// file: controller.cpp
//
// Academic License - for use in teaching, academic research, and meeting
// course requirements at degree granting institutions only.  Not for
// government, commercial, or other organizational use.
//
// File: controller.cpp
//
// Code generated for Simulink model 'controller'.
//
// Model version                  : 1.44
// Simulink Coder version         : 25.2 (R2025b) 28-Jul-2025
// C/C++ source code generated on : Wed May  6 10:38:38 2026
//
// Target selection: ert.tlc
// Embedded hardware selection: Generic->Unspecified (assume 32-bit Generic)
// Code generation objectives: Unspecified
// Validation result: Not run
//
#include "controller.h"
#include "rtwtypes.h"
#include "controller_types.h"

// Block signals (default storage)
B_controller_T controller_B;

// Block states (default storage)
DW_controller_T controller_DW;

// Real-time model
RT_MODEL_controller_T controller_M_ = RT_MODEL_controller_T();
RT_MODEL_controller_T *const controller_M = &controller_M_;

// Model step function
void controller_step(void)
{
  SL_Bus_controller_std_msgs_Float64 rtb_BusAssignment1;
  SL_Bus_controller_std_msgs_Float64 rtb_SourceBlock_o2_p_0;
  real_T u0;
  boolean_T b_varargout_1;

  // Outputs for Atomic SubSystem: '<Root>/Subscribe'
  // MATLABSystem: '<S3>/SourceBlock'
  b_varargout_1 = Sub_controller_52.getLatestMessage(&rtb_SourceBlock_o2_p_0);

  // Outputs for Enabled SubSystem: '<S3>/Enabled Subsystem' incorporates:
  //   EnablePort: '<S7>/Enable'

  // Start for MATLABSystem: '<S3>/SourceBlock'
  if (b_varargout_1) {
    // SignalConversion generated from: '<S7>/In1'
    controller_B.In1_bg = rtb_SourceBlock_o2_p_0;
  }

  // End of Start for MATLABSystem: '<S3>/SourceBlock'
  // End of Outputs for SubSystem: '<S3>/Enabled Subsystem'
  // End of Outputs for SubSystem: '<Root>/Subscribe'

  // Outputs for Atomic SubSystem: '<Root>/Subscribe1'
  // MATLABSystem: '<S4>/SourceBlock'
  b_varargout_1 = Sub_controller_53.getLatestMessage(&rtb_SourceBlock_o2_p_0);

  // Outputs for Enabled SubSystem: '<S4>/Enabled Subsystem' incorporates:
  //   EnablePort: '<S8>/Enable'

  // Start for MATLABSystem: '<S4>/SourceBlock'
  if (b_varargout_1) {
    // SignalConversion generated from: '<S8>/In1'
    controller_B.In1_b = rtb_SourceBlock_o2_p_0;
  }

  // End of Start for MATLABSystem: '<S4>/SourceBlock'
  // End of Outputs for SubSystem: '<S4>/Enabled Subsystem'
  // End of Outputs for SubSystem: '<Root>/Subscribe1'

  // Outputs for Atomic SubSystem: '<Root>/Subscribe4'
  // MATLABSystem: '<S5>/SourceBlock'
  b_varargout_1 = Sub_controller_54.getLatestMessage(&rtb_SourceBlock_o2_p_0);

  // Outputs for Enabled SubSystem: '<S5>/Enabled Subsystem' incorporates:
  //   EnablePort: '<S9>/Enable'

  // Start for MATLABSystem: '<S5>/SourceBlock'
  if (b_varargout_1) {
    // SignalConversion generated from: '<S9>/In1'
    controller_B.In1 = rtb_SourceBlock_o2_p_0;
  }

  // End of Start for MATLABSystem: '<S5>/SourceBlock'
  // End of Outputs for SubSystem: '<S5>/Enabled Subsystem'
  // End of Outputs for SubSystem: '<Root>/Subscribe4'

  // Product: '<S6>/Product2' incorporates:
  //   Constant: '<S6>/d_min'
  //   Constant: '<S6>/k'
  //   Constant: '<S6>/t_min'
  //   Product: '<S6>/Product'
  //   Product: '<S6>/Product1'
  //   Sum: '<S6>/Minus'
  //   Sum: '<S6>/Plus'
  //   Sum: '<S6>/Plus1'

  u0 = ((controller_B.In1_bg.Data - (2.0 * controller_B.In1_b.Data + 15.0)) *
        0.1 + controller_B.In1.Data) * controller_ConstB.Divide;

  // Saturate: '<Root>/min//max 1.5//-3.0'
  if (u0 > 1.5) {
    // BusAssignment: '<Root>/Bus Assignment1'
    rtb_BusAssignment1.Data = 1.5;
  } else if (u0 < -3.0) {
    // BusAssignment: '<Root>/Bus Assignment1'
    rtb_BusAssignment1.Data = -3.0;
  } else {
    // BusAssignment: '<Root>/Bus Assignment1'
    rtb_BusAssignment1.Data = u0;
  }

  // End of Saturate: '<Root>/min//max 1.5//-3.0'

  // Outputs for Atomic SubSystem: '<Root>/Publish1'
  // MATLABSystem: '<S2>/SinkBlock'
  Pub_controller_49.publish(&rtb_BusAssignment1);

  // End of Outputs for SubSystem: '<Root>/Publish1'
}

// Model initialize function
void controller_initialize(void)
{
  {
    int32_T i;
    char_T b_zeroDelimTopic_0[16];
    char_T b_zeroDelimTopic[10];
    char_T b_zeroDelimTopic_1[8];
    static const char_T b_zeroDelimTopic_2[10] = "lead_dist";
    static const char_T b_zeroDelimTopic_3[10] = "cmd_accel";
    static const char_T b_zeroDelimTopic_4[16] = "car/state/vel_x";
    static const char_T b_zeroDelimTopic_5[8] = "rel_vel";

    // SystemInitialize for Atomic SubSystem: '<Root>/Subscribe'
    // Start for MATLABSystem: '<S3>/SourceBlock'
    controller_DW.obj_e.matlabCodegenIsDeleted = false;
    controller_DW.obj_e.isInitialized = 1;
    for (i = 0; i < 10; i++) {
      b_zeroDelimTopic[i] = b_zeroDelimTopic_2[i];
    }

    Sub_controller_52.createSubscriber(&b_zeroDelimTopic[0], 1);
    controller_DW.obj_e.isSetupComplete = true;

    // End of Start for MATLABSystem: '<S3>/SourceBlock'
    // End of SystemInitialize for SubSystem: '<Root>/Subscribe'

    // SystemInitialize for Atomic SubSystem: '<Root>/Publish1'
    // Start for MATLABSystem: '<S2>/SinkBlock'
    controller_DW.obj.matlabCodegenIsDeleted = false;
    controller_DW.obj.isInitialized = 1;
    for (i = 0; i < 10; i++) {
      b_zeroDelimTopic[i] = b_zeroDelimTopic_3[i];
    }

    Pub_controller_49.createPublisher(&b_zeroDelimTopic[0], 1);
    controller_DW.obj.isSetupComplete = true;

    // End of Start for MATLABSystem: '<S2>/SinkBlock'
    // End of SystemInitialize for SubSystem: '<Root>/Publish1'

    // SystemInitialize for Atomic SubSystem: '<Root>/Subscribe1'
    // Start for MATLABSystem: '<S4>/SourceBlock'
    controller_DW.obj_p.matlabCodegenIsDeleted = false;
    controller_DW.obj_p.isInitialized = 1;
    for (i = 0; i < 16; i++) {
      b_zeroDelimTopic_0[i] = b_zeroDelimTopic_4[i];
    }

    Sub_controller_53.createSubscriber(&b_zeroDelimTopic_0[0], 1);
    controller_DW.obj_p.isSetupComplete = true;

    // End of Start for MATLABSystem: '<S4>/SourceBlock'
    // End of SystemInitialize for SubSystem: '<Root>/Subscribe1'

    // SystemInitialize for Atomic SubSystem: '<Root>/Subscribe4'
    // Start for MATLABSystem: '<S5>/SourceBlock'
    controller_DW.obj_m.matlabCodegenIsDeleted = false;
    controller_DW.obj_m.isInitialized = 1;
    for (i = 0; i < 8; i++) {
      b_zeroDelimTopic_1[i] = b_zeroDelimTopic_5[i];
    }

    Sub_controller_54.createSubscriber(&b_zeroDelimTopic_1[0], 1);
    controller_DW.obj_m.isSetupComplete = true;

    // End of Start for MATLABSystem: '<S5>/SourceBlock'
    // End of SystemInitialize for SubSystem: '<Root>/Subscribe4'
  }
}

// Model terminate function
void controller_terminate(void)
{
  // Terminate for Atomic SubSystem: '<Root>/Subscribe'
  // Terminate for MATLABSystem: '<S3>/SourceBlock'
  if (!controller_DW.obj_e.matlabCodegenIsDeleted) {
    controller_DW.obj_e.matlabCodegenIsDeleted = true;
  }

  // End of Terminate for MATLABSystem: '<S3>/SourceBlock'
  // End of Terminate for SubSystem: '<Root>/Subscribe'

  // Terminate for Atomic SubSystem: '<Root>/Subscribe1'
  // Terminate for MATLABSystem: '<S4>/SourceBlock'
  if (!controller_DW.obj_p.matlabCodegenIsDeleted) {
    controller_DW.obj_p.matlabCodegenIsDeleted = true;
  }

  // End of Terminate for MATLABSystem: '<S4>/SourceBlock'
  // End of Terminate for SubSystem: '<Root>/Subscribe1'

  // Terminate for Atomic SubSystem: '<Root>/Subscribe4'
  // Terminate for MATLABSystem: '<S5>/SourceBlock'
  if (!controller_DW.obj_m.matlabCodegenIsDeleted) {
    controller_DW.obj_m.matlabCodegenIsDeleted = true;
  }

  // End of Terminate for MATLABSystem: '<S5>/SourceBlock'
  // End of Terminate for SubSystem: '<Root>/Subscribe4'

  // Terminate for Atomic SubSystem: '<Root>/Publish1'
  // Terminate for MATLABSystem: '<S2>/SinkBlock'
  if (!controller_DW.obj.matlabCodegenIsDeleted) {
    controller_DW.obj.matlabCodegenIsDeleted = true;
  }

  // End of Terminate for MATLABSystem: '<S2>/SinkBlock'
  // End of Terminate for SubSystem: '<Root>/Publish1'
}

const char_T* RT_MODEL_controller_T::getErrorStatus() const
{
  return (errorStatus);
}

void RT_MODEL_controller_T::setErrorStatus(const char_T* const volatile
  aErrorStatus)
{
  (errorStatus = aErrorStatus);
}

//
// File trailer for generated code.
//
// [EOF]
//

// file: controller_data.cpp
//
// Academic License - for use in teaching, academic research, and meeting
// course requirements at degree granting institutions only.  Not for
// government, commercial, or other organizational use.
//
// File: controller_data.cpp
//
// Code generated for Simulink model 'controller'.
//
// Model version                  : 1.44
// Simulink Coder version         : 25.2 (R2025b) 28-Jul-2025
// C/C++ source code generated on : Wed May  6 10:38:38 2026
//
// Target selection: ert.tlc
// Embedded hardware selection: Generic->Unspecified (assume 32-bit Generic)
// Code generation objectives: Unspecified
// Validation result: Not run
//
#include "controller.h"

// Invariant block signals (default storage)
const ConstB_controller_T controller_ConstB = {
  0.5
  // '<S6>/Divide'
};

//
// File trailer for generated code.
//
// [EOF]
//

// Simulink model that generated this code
simulink model "controller"  (R2025b)
settings: Solver=FixedStepAuto  StartTime=0.0  StopTime=inf  FixedStep=0.05  RelTol=1e-3
libraries: robotlib x5

== system controller ==
  note: This block subscribes
      | to relative distance
  Blank Message1 : robotlib/Blank Message  messageClass=Message  entityType=std_msgs/Float64  messageType=std_msgs/Float64  SampleTime=inf  legacyBusStruct=off
  Bus Assignment1 : BusAssignment  AssignedSignals=Data
  Bus Selector1 : BusSelector  OutputSignals=Data
  Bus Selector4 : BusSelector  OutputSignals=Data
  Bus Selector6 : BusSelector  OutputSignals=Data
  Publish1 : robotlib/Publish  topicSource=Specify your own  topic=cmd_accel  messageType=std_msgs/Float64  legacyBusStruct=off  messageQueueLength=1
  Subscribe : robotlib/Subscribe  topicSource=Specify your own  topic=lead_dist  messageType=std_msgs/Float64  SampleTime=-1  legacyBusStruct=off  messageQueueLength=1
  Subscribe1 : robotlib/Subscribe  topicSource=Specify your own  topic=car/state/vel_x  messageType=std_msgs/Float64  SampleTime=-1  legacyBusStruct=off  messageQueueLength=1
  Subscribe4 : robotlib/Subscribe  topicSource=Specify your own  topic=rel_vel  messageType=std_msgs/Float64  SampleTime=-1  legacyBusStruct=off  messageQueueLength=1
  Terminator1 : Terminator
  Terminator2 : Terminator
  Terminator3 : Terminator
  controller_subsystem : Subsystem  ReferencedSubsystem=controller_subsystem
  min/max 1.5/-3.0 : Saturate  UpperLimit=1.5  LowerLimit=-3.0
  wires:
  Bus Assignment1/1 -> Publish1/1
  Subscribe1/2 -> Bus Selector1/1
  Subscribe4/2 -> Bus Selector4/1
  Subscribe/2 -> Bus Selector6/1
  Subscribe1/1 -> Terminator1/1
  min/max 1.5/-3.0/1 -> Bus Assignment1/2
  Subscribe4/1 -> Terminator2/1
  Subscribe/1 -> Terminator3/1
  Blank Message1/1 -> Bus Assignment1/1
  Bus Selector6/1 -> controller_subsystem/2  "<Data>"
  Bus Selector4/1 -> controller_subsystem/3  "<Data>"
  Bus Selector1/1 -> controller_subsystem/1  "<Data>"
  controller_subsystem/1 -> min/max 1.5/-3.0/1
